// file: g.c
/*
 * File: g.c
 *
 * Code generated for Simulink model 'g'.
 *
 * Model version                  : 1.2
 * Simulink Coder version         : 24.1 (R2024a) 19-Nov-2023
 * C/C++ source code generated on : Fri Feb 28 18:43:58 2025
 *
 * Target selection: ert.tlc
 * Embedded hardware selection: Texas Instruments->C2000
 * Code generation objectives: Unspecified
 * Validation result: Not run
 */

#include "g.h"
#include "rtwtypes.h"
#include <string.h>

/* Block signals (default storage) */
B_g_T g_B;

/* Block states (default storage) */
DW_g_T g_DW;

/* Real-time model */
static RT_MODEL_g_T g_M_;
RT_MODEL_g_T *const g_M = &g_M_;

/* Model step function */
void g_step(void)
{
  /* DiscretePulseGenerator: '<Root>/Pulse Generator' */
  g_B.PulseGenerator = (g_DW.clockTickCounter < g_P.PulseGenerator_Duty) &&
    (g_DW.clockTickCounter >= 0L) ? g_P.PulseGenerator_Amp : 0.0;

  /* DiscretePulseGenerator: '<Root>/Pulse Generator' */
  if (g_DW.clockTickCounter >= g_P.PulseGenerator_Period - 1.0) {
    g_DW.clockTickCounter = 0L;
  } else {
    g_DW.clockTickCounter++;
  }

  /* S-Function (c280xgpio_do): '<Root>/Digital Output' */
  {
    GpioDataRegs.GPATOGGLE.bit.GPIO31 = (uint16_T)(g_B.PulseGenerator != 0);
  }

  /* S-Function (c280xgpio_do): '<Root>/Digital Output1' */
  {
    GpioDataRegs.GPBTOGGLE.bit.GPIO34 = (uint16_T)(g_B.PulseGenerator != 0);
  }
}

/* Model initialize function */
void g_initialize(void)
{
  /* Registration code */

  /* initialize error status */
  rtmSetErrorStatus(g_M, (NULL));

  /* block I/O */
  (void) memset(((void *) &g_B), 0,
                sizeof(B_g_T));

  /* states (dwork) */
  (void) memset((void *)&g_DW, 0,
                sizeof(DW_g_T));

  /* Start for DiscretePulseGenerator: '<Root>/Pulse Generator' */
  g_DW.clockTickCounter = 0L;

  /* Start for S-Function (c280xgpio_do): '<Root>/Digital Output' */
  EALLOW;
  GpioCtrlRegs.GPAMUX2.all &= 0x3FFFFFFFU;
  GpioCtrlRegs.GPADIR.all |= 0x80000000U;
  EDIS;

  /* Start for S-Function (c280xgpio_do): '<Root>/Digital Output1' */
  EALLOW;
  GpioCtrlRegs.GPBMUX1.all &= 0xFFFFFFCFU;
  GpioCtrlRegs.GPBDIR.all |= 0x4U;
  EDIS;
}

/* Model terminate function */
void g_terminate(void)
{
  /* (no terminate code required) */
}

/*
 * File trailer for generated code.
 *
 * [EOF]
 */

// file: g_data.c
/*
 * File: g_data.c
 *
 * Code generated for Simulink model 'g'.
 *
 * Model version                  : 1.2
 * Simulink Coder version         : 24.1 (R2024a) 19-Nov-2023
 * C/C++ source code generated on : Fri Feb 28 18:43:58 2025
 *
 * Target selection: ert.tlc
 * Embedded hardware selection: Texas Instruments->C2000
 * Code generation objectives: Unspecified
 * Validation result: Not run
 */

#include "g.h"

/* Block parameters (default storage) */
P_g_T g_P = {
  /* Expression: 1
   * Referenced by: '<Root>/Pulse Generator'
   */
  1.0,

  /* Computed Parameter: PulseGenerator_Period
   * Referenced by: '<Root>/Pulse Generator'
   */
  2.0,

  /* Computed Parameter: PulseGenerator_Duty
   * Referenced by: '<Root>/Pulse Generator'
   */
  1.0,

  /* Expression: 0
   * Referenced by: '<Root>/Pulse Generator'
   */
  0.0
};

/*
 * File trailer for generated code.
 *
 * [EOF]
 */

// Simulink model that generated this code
simulink model "g"  (R2024a)
settings: Solver=FixedStepAuto  StartTime=0.0  StopTime=Inf  RelTol=1e-3  EnableMultiTasking=on
libraries: c2837xDlib x2

== system g ==
  Digital Output : c2837xDlib/Digital Output  GPIO_Number=GPIO24~GPIO31  GPIO_Bit0=off  GPIO_BIT0_Toggle=off  GPIO_Bit1=off  GPIO_BIT1_Toggle=off  GPIO_Bit2=off  GPIO_BIT2_Toggle=off  GPIO_Bit3=off  GPIO_BIT3_Toggle=off  GPIO_Bit4=off  GPIO_BIT4_Toggle=off  GPIO_Bit5=off  GPIO_BIT5_Toggle=off  GPIO_Bit6=off  GPIO_BIT6_Toggle=off  GPIO_Bit7=on  GPIO_BIT7_Toggle=on
  Digital Output1 : c2837xDlib/Digital Output  GPIO_Number=GPIO32~GPIO39  GPIO_Bit0=off  GPIO_BIT0_Toggle=off  GPIO_Bit1=off  GPIO_BIT1_Toggle=off  GPIO_Bit2=on  GPIO_BIT2_Toggle=on  GPIO_Bit3=off  GPIO_BIT3_Toggle=off  GPIO_Bit4=off  GPIO_BIT4_Toggle=off  GPIO_Bit5=off  GPIO_BIT5_Toggle=off  GPIO_Bit6=off  GPIO_BIT6_Toggle=off  GPIO_Bit7=off  GPIO_BIT7_Toggle=off
  Pulse Generator : DiscretePulseGenerator  PulseType=Time based  Period=1  PulseWidth=50
  wires:
  Pulse Generator/1 -> Digital Output1/1, Digital Output/1
